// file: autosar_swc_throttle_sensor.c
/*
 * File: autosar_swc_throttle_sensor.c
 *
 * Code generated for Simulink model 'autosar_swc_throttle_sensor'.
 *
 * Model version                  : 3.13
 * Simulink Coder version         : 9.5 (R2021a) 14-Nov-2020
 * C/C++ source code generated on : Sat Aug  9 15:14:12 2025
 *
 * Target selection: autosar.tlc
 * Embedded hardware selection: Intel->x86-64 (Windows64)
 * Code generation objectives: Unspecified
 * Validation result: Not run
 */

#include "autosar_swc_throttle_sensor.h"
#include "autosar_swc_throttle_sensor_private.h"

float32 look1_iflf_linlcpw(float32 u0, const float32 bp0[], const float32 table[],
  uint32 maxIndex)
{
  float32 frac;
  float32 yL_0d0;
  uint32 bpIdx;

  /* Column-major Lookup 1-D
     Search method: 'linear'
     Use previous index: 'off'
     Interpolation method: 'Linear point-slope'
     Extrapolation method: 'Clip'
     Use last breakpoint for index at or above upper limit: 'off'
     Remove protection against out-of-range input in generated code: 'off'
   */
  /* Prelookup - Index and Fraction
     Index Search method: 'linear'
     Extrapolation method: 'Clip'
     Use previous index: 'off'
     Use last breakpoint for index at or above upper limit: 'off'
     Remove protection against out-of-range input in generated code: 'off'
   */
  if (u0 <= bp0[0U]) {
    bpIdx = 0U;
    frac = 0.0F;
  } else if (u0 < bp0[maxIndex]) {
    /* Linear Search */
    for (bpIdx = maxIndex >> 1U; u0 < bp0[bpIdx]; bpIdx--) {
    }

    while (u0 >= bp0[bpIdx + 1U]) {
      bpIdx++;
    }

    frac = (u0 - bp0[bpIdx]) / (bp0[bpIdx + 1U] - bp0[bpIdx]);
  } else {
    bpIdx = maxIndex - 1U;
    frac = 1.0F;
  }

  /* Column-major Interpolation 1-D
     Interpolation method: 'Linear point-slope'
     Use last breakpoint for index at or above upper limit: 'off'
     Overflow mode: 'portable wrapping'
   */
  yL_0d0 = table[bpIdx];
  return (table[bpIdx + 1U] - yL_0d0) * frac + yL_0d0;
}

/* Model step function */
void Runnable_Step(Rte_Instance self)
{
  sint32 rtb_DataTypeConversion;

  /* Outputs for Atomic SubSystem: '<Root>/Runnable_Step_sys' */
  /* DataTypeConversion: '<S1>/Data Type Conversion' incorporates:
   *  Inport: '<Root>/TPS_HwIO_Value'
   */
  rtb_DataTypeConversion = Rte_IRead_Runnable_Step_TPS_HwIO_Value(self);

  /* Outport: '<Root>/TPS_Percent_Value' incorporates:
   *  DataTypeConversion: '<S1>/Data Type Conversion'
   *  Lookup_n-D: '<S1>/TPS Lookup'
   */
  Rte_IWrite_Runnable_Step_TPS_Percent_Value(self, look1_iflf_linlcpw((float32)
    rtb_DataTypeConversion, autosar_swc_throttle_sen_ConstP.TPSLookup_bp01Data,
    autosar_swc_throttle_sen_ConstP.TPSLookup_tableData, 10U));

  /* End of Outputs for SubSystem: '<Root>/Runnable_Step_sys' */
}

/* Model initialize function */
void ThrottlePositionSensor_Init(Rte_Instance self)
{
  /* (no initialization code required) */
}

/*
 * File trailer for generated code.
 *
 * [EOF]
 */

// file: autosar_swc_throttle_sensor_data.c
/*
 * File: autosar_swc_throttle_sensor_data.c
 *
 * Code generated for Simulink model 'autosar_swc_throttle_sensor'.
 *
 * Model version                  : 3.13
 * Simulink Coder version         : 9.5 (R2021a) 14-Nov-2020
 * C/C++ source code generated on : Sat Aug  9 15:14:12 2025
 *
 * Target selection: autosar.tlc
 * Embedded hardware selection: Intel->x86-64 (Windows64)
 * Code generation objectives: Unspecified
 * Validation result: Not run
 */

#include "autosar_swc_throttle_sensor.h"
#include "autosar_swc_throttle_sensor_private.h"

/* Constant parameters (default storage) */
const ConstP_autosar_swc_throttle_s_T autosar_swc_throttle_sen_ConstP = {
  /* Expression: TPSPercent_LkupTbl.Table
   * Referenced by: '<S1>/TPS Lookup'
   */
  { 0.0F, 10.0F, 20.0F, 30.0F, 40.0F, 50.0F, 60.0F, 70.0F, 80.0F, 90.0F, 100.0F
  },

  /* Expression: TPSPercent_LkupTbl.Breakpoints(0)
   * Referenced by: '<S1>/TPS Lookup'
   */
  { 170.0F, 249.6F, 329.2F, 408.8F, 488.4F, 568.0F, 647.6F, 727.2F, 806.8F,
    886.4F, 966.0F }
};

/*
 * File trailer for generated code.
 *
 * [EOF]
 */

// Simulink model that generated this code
simulink model "autosar_swc_throttle_sensor"  (R2021a)
settings: Solver=FixedStepDiscrete  StartTime=0.0  StopTime=10.0  FixedStep=0.005  RelTol=1e-3
model workspace (MATLAB code in the model file):
  | TPSPercent_LkupTbl = Simulink.LookupTable;
  | TPSPercent_LkupTbl.Table.DataType = 'single';
  | TPSPercent_LkupTbl.Table.Min = [];
  | TPSPercent_LkupTbl.Table.Max = [];
  | TPSPercent_LkupTbl.Table.Unit = '';
  | TPSPercent_LkupTbl.Table.FieldName = 'Table';
  | TPSPercent_LkupTbl.Table.Description = '';
  | TPSPercent_LkupTbl.Table.Value = ...
  |   [0 10 20 30 40 50 60 70 80 90 100];
  | TPSPercent_LkupTbl.BreakpointsSpecification = 'Explicit values';
  | TPSPercent_LkupTbl.SupportTunableSize = false;
  | TPSPercent_LkupTbl.Breakpoints.DataType = 'single';
  | TPSPercent_LkupTbl.Breakpoints.Min = [];
  | TPSPercent_LkupTbl.Breakpoints.Max = [];
  | TPSPercent_LkupTbl.Breakpoints.Unit = '';
  | TPSPercent_LkupTbl.Breakpoints.FieldName = 'BP1';
  | TPSPercent_LkupTbl.Breakpoints.Description = '';
  | TPSPercent_LkupTbl.Breakpoints.Value = single(linspace(170, 966, 11));
  | TPSPercent_LkupTbl.Breakpoints.TunableSizeName = 'N1';
  | TPSPercent_LkupTbl.CoderInfo.StorageClass = 'Auto';
  | TPSPercent_LkupTbl.StructTypeInfo.Name = 'MyStruct';
  | TPSPercent_LkupTbl.StructTypeInfo.DataScope = 'Auto';
  | TPSPercent_LkupTbl.StructTypeInfo.HeaderFileName = 'Rte_Type.h';
undefined symbols (not defined in the file): TPSPercentBkpt, TPSPercentTbl

== system autosar_swc_throttle_sensor ==
  note: Copyright 2017-2019 The MathWorks, Inc.
  TPS_HwIO_Value : Inport  OutDataTypeStr=uint16  PortDimensions=1
  Runnable_Step_sys : Subsystem  TreatAsAtomicUnit=on  SystemSampleTime=0.005
  TPS_Percent_Value : Outport  OutDataTypeStr=single  PortDimensions=1  VectorParamsAs1DForOutWhenUnconnected=off
  Scope : Scope
  wires:
  TPS_HwIO_Value/1 -> Runnable_Step_sys/1(TPS_HwIO_Value_read)
  Runnable_Step_sys/1(TPS_Percent_Value_write) -> TPS_Percent_Value/1

== system autosar_swc_throttle_sensor/Runnable_Step_sys ==
  TPS_HwIO_Value_read : Inport
  Data Type Conversion : DataTypeConversion  OutDataTypeStr=single
  TPS Lookup : Lookup_n-D  NumberOfTableDimensions=1  DataSpecification=Lookup table object  LookupTableObject=TPSPercent_LkupTbl  BreakpointsForDimension1=TPSPercentBkpt  BreakpointsForDimension1DataTypeStr=single  IndexSearchMethod=Linear search  Table=TPSPercentTbl  TableDataTypeStr=single  ExtrapMethod=Clip  InternalRulePriority=Speed  OutDataTypeStr=single  RndMeth=Simplest  InputSameDT=on
  TPS_Percent_Value_write : Outport  VectorParamsAs1DForOutWhenUnconnected=off
  wires:
  TPS_HwIO_Value_read/1 -> Data Type Conversion/1
  TPS Lookup/1 -> TPS_Percent_Value_write/1
  Data Type Conversion/1 -> TPS Lookup/1
